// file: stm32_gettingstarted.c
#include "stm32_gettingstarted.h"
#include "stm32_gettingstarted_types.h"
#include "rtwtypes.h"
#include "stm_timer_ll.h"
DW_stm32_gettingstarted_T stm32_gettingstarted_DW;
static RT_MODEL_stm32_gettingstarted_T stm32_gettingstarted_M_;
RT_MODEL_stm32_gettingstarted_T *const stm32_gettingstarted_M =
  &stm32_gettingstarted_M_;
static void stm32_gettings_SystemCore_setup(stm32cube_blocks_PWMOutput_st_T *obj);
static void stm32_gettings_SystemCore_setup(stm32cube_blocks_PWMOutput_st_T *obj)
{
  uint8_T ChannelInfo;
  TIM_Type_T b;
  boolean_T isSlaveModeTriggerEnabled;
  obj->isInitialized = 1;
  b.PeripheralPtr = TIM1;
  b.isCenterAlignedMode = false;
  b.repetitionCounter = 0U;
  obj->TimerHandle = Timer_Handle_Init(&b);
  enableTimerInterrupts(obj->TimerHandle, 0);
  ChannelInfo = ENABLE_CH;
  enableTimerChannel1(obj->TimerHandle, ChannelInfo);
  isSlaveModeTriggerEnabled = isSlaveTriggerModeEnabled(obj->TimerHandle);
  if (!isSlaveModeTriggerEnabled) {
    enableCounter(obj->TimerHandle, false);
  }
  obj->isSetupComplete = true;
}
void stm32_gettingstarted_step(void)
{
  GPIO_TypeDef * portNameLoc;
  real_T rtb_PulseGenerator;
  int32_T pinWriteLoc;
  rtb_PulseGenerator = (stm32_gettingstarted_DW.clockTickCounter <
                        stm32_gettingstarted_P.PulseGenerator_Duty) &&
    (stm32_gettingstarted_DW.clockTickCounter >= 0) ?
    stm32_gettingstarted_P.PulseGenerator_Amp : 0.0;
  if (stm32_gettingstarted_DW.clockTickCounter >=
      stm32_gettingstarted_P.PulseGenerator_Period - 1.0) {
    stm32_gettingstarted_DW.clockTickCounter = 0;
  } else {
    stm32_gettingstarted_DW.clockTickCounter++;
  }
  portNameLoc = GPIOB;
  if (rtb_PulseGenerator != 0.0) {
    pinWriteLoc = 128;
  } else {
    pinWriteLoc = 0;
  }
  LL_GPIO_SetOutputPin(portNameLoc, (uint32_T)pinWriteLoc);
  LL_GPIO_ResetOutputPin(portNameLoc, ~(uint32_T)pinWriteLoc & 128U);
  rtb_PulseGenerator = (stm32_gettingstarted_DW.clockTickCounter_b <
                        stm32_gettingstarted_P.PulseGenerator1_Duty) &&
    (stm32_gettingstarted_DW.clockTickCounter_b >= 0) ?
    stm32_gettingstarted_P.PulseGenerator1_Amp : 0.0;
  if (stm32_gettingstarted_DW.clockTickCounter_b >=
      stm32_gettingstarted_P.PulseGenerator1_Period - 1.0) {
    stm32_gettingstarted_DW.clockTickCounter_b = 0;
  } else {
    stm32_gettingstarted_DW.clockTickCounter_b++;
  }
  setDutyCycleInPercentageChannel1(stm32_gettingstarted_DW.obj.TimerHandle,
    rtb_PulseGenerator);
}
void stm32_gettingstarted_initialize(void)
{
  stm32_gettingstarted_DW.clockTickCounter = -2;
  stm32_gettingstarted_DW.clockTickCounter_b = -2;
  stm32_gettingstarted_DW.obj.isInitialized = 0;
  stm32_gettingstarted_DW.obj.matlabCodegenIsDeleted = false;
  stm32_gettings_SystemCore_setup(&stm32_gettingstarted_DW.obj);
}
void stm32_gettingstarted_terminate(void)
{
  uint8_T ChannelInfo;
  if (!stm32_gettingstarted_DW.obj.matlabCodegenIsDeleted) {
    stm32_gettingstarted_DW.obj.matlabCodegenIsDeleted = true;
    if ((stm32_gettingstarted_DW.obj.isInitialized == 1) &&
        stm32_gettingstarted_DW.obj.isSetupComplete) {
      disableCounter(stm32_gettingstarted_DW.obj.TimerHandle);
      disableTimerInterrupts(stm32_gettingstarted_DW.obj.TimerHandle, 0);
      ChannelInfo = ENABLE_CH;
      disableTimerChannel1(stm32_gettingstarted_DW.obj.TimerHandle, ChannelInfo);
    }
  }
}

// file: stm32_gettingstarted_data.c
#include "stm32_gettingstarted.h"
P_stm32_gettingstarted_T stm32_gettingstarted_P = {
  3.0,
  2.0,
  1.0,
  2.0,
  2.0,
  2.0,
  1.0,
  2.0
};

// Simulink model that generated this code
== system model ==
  DigitalPortWrite#1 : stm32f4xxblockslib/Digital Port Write  <- 1: PulseGenerator
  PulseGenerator : DiscretePulseGenerator  Amplitude=3  PhaseDelay=2
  PWMOutput : stm32f7xxblockslib/PWM Output  <- 1: PulseGenerator1
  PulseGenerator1 : DiscretePulseGenerator  Amplitude=2  PhaseDelay=2
